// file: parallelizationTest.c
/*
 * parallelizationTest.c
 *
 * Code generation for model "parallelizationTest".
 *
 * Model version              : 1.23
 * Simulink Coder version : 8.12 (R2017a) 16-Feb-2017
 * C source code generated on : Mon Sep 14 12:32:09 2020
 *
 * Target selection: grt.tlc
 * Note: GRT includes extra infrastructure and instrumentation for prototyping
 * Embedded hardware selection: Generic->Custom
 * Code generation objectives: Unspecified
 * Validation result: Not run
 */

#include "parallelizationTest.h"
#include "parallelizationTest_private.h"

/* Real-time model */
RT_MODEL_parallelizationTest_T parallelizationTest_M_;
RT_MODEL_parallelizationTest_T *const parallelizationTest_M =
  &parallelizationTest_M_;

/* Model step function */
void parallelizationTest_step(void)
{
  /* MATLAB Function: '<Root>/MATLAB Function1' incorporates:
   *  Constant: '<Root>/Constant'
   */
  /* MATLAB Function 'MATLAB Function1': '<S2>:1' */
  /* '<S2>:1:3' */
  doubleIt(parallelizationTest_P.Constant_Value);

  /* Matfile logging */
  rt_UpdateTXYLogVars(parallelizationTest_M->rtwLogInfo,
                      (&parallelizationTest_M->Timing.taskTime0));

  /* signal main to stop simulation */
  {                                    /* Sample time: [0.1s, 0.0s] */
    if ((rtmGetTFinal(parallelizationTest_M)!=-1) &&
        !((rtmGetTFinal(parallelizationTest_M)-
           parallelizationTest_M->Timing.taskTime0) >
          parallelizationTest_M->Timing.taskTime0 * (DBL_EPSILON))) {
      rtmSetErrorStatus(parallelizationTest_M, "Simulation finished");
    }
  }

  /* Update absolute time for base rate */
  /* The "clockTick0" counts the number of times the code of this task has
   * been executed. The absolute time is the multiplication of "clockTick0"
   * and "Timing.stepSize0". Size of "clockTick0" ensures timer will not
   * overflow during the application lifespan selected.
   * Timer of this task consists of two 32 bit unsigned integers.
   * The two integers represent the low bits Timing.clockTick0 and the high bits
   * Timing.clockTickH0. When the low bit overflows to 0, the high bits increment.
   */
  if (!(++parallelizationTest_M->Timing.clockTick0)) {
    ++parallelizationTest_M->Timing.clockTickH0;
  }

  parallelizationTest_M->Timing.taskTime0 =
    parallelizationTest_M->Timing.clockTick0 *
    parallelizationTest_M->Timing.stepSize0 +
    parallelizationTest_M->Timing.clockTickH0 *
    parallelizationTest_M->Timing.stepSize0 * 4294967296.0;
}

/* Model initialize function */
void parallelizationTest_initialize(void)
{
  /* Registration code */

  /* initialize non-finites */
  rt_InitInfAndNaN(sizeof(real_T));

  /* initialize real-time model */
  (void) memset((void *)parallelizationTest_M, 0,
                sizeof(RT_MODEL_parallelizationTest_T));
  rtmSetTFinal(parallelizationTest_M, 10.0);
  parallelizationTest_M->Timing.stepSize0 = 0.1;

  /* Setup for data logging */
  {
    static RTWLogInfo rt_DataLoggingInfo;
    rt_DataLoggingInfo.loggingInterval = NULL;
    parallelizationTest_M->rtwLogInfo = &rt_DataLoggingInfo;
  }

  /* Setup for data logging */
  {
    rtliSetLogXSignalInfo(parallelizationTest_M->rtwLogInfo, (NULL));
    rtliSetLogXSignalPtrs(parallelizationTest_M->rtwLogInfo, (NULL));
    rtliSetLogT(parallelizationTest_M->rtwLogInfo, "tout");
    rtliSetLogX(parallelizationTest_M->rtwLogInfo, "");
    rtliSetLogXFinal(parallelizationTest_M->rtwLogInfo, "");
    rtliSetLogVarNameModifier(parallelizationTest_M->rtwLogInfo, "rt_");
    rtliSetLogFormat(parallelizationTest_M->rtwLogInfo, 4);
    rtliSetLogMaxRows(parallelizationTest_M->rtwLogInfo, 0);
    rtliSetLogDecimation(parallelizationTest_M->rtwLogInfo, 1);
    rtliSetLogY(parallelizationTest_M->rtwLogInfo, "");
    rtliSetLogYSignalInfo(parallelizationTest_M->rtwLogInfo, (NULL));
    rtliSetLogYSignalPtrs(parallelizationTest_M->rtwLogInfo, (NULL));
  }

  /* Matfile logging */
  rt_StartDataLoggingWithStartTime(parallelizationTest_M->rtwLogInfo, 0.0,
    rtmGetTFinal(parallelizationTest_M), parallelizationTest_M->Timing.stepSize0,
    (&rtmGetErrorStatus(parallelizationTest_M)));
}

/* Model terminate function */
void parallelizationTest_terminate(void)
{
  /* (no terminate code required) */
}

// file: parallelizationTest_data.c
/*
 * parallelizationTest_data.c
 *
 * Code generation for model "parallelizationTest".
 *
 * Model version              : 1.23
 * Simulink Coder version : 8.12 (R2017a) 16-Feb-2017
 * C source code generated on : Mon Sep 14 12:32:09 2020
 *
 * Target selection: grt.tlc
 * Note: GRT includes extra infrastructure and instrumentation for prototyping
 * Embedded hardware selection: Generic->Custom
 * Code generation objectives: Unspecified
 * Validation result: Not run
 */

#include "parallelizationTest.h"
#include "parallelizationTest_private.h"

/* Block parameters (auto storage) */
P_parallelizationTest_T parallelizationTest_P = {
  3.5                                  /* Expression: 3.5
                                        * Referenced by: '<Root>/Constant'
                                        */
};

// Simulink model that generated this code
simulink model "parallelizationTest"  (R2017a)
settings: Solver=FixedStepAuto  StartTime=0.0  StopTime=10  FixedStep=0.1  RelTol=1e-3

== system parallelizationTest ==
  Constant : Constant  Value=3.5
  Display1 : Display
  MATLAB Function : MATLAB Function  Commented=on  TreatAsAtomicUnit=on
  MATLAB Function1 : MATLAB Function  TreatAsAtomicUnit=on
  To Workspace : ToWorkspace  Commented=on  VariableName=simout  SaveFormat=Timeseries  SampleTime=-1
  matrix_size : Constant  Commented=on  Value=500
  repeat_times : Constant  Commented=on  Value=15
  wires:
  matrix_size/1 -> MATLAB Function/1(matrix_size)
  repeat_times/1 -> MATLAB Function/2(repeat_times)
  MATLAB Function/1(status) -> To Workspace/1
  Constant/1 -> MATLAB Function1/1(u)
  MATLAB Function1/1(y) -> Display1/1

== matlab function parallelizationTest/MATLAB Function1 ==
function y = callingDoubleIt(u)
y = 0.0;
y = coder.ceval('doubleIt',u);

== matlab function parallelizationTest/MATLAB Function ==
function status = time_par_tests(matrix_size, repeat_times)
% time_par_tests: Perform a parallization test (baseline)

status = 0;
status = coder.ceval('time_par_tests',matrix_size, repeat_times);

end
